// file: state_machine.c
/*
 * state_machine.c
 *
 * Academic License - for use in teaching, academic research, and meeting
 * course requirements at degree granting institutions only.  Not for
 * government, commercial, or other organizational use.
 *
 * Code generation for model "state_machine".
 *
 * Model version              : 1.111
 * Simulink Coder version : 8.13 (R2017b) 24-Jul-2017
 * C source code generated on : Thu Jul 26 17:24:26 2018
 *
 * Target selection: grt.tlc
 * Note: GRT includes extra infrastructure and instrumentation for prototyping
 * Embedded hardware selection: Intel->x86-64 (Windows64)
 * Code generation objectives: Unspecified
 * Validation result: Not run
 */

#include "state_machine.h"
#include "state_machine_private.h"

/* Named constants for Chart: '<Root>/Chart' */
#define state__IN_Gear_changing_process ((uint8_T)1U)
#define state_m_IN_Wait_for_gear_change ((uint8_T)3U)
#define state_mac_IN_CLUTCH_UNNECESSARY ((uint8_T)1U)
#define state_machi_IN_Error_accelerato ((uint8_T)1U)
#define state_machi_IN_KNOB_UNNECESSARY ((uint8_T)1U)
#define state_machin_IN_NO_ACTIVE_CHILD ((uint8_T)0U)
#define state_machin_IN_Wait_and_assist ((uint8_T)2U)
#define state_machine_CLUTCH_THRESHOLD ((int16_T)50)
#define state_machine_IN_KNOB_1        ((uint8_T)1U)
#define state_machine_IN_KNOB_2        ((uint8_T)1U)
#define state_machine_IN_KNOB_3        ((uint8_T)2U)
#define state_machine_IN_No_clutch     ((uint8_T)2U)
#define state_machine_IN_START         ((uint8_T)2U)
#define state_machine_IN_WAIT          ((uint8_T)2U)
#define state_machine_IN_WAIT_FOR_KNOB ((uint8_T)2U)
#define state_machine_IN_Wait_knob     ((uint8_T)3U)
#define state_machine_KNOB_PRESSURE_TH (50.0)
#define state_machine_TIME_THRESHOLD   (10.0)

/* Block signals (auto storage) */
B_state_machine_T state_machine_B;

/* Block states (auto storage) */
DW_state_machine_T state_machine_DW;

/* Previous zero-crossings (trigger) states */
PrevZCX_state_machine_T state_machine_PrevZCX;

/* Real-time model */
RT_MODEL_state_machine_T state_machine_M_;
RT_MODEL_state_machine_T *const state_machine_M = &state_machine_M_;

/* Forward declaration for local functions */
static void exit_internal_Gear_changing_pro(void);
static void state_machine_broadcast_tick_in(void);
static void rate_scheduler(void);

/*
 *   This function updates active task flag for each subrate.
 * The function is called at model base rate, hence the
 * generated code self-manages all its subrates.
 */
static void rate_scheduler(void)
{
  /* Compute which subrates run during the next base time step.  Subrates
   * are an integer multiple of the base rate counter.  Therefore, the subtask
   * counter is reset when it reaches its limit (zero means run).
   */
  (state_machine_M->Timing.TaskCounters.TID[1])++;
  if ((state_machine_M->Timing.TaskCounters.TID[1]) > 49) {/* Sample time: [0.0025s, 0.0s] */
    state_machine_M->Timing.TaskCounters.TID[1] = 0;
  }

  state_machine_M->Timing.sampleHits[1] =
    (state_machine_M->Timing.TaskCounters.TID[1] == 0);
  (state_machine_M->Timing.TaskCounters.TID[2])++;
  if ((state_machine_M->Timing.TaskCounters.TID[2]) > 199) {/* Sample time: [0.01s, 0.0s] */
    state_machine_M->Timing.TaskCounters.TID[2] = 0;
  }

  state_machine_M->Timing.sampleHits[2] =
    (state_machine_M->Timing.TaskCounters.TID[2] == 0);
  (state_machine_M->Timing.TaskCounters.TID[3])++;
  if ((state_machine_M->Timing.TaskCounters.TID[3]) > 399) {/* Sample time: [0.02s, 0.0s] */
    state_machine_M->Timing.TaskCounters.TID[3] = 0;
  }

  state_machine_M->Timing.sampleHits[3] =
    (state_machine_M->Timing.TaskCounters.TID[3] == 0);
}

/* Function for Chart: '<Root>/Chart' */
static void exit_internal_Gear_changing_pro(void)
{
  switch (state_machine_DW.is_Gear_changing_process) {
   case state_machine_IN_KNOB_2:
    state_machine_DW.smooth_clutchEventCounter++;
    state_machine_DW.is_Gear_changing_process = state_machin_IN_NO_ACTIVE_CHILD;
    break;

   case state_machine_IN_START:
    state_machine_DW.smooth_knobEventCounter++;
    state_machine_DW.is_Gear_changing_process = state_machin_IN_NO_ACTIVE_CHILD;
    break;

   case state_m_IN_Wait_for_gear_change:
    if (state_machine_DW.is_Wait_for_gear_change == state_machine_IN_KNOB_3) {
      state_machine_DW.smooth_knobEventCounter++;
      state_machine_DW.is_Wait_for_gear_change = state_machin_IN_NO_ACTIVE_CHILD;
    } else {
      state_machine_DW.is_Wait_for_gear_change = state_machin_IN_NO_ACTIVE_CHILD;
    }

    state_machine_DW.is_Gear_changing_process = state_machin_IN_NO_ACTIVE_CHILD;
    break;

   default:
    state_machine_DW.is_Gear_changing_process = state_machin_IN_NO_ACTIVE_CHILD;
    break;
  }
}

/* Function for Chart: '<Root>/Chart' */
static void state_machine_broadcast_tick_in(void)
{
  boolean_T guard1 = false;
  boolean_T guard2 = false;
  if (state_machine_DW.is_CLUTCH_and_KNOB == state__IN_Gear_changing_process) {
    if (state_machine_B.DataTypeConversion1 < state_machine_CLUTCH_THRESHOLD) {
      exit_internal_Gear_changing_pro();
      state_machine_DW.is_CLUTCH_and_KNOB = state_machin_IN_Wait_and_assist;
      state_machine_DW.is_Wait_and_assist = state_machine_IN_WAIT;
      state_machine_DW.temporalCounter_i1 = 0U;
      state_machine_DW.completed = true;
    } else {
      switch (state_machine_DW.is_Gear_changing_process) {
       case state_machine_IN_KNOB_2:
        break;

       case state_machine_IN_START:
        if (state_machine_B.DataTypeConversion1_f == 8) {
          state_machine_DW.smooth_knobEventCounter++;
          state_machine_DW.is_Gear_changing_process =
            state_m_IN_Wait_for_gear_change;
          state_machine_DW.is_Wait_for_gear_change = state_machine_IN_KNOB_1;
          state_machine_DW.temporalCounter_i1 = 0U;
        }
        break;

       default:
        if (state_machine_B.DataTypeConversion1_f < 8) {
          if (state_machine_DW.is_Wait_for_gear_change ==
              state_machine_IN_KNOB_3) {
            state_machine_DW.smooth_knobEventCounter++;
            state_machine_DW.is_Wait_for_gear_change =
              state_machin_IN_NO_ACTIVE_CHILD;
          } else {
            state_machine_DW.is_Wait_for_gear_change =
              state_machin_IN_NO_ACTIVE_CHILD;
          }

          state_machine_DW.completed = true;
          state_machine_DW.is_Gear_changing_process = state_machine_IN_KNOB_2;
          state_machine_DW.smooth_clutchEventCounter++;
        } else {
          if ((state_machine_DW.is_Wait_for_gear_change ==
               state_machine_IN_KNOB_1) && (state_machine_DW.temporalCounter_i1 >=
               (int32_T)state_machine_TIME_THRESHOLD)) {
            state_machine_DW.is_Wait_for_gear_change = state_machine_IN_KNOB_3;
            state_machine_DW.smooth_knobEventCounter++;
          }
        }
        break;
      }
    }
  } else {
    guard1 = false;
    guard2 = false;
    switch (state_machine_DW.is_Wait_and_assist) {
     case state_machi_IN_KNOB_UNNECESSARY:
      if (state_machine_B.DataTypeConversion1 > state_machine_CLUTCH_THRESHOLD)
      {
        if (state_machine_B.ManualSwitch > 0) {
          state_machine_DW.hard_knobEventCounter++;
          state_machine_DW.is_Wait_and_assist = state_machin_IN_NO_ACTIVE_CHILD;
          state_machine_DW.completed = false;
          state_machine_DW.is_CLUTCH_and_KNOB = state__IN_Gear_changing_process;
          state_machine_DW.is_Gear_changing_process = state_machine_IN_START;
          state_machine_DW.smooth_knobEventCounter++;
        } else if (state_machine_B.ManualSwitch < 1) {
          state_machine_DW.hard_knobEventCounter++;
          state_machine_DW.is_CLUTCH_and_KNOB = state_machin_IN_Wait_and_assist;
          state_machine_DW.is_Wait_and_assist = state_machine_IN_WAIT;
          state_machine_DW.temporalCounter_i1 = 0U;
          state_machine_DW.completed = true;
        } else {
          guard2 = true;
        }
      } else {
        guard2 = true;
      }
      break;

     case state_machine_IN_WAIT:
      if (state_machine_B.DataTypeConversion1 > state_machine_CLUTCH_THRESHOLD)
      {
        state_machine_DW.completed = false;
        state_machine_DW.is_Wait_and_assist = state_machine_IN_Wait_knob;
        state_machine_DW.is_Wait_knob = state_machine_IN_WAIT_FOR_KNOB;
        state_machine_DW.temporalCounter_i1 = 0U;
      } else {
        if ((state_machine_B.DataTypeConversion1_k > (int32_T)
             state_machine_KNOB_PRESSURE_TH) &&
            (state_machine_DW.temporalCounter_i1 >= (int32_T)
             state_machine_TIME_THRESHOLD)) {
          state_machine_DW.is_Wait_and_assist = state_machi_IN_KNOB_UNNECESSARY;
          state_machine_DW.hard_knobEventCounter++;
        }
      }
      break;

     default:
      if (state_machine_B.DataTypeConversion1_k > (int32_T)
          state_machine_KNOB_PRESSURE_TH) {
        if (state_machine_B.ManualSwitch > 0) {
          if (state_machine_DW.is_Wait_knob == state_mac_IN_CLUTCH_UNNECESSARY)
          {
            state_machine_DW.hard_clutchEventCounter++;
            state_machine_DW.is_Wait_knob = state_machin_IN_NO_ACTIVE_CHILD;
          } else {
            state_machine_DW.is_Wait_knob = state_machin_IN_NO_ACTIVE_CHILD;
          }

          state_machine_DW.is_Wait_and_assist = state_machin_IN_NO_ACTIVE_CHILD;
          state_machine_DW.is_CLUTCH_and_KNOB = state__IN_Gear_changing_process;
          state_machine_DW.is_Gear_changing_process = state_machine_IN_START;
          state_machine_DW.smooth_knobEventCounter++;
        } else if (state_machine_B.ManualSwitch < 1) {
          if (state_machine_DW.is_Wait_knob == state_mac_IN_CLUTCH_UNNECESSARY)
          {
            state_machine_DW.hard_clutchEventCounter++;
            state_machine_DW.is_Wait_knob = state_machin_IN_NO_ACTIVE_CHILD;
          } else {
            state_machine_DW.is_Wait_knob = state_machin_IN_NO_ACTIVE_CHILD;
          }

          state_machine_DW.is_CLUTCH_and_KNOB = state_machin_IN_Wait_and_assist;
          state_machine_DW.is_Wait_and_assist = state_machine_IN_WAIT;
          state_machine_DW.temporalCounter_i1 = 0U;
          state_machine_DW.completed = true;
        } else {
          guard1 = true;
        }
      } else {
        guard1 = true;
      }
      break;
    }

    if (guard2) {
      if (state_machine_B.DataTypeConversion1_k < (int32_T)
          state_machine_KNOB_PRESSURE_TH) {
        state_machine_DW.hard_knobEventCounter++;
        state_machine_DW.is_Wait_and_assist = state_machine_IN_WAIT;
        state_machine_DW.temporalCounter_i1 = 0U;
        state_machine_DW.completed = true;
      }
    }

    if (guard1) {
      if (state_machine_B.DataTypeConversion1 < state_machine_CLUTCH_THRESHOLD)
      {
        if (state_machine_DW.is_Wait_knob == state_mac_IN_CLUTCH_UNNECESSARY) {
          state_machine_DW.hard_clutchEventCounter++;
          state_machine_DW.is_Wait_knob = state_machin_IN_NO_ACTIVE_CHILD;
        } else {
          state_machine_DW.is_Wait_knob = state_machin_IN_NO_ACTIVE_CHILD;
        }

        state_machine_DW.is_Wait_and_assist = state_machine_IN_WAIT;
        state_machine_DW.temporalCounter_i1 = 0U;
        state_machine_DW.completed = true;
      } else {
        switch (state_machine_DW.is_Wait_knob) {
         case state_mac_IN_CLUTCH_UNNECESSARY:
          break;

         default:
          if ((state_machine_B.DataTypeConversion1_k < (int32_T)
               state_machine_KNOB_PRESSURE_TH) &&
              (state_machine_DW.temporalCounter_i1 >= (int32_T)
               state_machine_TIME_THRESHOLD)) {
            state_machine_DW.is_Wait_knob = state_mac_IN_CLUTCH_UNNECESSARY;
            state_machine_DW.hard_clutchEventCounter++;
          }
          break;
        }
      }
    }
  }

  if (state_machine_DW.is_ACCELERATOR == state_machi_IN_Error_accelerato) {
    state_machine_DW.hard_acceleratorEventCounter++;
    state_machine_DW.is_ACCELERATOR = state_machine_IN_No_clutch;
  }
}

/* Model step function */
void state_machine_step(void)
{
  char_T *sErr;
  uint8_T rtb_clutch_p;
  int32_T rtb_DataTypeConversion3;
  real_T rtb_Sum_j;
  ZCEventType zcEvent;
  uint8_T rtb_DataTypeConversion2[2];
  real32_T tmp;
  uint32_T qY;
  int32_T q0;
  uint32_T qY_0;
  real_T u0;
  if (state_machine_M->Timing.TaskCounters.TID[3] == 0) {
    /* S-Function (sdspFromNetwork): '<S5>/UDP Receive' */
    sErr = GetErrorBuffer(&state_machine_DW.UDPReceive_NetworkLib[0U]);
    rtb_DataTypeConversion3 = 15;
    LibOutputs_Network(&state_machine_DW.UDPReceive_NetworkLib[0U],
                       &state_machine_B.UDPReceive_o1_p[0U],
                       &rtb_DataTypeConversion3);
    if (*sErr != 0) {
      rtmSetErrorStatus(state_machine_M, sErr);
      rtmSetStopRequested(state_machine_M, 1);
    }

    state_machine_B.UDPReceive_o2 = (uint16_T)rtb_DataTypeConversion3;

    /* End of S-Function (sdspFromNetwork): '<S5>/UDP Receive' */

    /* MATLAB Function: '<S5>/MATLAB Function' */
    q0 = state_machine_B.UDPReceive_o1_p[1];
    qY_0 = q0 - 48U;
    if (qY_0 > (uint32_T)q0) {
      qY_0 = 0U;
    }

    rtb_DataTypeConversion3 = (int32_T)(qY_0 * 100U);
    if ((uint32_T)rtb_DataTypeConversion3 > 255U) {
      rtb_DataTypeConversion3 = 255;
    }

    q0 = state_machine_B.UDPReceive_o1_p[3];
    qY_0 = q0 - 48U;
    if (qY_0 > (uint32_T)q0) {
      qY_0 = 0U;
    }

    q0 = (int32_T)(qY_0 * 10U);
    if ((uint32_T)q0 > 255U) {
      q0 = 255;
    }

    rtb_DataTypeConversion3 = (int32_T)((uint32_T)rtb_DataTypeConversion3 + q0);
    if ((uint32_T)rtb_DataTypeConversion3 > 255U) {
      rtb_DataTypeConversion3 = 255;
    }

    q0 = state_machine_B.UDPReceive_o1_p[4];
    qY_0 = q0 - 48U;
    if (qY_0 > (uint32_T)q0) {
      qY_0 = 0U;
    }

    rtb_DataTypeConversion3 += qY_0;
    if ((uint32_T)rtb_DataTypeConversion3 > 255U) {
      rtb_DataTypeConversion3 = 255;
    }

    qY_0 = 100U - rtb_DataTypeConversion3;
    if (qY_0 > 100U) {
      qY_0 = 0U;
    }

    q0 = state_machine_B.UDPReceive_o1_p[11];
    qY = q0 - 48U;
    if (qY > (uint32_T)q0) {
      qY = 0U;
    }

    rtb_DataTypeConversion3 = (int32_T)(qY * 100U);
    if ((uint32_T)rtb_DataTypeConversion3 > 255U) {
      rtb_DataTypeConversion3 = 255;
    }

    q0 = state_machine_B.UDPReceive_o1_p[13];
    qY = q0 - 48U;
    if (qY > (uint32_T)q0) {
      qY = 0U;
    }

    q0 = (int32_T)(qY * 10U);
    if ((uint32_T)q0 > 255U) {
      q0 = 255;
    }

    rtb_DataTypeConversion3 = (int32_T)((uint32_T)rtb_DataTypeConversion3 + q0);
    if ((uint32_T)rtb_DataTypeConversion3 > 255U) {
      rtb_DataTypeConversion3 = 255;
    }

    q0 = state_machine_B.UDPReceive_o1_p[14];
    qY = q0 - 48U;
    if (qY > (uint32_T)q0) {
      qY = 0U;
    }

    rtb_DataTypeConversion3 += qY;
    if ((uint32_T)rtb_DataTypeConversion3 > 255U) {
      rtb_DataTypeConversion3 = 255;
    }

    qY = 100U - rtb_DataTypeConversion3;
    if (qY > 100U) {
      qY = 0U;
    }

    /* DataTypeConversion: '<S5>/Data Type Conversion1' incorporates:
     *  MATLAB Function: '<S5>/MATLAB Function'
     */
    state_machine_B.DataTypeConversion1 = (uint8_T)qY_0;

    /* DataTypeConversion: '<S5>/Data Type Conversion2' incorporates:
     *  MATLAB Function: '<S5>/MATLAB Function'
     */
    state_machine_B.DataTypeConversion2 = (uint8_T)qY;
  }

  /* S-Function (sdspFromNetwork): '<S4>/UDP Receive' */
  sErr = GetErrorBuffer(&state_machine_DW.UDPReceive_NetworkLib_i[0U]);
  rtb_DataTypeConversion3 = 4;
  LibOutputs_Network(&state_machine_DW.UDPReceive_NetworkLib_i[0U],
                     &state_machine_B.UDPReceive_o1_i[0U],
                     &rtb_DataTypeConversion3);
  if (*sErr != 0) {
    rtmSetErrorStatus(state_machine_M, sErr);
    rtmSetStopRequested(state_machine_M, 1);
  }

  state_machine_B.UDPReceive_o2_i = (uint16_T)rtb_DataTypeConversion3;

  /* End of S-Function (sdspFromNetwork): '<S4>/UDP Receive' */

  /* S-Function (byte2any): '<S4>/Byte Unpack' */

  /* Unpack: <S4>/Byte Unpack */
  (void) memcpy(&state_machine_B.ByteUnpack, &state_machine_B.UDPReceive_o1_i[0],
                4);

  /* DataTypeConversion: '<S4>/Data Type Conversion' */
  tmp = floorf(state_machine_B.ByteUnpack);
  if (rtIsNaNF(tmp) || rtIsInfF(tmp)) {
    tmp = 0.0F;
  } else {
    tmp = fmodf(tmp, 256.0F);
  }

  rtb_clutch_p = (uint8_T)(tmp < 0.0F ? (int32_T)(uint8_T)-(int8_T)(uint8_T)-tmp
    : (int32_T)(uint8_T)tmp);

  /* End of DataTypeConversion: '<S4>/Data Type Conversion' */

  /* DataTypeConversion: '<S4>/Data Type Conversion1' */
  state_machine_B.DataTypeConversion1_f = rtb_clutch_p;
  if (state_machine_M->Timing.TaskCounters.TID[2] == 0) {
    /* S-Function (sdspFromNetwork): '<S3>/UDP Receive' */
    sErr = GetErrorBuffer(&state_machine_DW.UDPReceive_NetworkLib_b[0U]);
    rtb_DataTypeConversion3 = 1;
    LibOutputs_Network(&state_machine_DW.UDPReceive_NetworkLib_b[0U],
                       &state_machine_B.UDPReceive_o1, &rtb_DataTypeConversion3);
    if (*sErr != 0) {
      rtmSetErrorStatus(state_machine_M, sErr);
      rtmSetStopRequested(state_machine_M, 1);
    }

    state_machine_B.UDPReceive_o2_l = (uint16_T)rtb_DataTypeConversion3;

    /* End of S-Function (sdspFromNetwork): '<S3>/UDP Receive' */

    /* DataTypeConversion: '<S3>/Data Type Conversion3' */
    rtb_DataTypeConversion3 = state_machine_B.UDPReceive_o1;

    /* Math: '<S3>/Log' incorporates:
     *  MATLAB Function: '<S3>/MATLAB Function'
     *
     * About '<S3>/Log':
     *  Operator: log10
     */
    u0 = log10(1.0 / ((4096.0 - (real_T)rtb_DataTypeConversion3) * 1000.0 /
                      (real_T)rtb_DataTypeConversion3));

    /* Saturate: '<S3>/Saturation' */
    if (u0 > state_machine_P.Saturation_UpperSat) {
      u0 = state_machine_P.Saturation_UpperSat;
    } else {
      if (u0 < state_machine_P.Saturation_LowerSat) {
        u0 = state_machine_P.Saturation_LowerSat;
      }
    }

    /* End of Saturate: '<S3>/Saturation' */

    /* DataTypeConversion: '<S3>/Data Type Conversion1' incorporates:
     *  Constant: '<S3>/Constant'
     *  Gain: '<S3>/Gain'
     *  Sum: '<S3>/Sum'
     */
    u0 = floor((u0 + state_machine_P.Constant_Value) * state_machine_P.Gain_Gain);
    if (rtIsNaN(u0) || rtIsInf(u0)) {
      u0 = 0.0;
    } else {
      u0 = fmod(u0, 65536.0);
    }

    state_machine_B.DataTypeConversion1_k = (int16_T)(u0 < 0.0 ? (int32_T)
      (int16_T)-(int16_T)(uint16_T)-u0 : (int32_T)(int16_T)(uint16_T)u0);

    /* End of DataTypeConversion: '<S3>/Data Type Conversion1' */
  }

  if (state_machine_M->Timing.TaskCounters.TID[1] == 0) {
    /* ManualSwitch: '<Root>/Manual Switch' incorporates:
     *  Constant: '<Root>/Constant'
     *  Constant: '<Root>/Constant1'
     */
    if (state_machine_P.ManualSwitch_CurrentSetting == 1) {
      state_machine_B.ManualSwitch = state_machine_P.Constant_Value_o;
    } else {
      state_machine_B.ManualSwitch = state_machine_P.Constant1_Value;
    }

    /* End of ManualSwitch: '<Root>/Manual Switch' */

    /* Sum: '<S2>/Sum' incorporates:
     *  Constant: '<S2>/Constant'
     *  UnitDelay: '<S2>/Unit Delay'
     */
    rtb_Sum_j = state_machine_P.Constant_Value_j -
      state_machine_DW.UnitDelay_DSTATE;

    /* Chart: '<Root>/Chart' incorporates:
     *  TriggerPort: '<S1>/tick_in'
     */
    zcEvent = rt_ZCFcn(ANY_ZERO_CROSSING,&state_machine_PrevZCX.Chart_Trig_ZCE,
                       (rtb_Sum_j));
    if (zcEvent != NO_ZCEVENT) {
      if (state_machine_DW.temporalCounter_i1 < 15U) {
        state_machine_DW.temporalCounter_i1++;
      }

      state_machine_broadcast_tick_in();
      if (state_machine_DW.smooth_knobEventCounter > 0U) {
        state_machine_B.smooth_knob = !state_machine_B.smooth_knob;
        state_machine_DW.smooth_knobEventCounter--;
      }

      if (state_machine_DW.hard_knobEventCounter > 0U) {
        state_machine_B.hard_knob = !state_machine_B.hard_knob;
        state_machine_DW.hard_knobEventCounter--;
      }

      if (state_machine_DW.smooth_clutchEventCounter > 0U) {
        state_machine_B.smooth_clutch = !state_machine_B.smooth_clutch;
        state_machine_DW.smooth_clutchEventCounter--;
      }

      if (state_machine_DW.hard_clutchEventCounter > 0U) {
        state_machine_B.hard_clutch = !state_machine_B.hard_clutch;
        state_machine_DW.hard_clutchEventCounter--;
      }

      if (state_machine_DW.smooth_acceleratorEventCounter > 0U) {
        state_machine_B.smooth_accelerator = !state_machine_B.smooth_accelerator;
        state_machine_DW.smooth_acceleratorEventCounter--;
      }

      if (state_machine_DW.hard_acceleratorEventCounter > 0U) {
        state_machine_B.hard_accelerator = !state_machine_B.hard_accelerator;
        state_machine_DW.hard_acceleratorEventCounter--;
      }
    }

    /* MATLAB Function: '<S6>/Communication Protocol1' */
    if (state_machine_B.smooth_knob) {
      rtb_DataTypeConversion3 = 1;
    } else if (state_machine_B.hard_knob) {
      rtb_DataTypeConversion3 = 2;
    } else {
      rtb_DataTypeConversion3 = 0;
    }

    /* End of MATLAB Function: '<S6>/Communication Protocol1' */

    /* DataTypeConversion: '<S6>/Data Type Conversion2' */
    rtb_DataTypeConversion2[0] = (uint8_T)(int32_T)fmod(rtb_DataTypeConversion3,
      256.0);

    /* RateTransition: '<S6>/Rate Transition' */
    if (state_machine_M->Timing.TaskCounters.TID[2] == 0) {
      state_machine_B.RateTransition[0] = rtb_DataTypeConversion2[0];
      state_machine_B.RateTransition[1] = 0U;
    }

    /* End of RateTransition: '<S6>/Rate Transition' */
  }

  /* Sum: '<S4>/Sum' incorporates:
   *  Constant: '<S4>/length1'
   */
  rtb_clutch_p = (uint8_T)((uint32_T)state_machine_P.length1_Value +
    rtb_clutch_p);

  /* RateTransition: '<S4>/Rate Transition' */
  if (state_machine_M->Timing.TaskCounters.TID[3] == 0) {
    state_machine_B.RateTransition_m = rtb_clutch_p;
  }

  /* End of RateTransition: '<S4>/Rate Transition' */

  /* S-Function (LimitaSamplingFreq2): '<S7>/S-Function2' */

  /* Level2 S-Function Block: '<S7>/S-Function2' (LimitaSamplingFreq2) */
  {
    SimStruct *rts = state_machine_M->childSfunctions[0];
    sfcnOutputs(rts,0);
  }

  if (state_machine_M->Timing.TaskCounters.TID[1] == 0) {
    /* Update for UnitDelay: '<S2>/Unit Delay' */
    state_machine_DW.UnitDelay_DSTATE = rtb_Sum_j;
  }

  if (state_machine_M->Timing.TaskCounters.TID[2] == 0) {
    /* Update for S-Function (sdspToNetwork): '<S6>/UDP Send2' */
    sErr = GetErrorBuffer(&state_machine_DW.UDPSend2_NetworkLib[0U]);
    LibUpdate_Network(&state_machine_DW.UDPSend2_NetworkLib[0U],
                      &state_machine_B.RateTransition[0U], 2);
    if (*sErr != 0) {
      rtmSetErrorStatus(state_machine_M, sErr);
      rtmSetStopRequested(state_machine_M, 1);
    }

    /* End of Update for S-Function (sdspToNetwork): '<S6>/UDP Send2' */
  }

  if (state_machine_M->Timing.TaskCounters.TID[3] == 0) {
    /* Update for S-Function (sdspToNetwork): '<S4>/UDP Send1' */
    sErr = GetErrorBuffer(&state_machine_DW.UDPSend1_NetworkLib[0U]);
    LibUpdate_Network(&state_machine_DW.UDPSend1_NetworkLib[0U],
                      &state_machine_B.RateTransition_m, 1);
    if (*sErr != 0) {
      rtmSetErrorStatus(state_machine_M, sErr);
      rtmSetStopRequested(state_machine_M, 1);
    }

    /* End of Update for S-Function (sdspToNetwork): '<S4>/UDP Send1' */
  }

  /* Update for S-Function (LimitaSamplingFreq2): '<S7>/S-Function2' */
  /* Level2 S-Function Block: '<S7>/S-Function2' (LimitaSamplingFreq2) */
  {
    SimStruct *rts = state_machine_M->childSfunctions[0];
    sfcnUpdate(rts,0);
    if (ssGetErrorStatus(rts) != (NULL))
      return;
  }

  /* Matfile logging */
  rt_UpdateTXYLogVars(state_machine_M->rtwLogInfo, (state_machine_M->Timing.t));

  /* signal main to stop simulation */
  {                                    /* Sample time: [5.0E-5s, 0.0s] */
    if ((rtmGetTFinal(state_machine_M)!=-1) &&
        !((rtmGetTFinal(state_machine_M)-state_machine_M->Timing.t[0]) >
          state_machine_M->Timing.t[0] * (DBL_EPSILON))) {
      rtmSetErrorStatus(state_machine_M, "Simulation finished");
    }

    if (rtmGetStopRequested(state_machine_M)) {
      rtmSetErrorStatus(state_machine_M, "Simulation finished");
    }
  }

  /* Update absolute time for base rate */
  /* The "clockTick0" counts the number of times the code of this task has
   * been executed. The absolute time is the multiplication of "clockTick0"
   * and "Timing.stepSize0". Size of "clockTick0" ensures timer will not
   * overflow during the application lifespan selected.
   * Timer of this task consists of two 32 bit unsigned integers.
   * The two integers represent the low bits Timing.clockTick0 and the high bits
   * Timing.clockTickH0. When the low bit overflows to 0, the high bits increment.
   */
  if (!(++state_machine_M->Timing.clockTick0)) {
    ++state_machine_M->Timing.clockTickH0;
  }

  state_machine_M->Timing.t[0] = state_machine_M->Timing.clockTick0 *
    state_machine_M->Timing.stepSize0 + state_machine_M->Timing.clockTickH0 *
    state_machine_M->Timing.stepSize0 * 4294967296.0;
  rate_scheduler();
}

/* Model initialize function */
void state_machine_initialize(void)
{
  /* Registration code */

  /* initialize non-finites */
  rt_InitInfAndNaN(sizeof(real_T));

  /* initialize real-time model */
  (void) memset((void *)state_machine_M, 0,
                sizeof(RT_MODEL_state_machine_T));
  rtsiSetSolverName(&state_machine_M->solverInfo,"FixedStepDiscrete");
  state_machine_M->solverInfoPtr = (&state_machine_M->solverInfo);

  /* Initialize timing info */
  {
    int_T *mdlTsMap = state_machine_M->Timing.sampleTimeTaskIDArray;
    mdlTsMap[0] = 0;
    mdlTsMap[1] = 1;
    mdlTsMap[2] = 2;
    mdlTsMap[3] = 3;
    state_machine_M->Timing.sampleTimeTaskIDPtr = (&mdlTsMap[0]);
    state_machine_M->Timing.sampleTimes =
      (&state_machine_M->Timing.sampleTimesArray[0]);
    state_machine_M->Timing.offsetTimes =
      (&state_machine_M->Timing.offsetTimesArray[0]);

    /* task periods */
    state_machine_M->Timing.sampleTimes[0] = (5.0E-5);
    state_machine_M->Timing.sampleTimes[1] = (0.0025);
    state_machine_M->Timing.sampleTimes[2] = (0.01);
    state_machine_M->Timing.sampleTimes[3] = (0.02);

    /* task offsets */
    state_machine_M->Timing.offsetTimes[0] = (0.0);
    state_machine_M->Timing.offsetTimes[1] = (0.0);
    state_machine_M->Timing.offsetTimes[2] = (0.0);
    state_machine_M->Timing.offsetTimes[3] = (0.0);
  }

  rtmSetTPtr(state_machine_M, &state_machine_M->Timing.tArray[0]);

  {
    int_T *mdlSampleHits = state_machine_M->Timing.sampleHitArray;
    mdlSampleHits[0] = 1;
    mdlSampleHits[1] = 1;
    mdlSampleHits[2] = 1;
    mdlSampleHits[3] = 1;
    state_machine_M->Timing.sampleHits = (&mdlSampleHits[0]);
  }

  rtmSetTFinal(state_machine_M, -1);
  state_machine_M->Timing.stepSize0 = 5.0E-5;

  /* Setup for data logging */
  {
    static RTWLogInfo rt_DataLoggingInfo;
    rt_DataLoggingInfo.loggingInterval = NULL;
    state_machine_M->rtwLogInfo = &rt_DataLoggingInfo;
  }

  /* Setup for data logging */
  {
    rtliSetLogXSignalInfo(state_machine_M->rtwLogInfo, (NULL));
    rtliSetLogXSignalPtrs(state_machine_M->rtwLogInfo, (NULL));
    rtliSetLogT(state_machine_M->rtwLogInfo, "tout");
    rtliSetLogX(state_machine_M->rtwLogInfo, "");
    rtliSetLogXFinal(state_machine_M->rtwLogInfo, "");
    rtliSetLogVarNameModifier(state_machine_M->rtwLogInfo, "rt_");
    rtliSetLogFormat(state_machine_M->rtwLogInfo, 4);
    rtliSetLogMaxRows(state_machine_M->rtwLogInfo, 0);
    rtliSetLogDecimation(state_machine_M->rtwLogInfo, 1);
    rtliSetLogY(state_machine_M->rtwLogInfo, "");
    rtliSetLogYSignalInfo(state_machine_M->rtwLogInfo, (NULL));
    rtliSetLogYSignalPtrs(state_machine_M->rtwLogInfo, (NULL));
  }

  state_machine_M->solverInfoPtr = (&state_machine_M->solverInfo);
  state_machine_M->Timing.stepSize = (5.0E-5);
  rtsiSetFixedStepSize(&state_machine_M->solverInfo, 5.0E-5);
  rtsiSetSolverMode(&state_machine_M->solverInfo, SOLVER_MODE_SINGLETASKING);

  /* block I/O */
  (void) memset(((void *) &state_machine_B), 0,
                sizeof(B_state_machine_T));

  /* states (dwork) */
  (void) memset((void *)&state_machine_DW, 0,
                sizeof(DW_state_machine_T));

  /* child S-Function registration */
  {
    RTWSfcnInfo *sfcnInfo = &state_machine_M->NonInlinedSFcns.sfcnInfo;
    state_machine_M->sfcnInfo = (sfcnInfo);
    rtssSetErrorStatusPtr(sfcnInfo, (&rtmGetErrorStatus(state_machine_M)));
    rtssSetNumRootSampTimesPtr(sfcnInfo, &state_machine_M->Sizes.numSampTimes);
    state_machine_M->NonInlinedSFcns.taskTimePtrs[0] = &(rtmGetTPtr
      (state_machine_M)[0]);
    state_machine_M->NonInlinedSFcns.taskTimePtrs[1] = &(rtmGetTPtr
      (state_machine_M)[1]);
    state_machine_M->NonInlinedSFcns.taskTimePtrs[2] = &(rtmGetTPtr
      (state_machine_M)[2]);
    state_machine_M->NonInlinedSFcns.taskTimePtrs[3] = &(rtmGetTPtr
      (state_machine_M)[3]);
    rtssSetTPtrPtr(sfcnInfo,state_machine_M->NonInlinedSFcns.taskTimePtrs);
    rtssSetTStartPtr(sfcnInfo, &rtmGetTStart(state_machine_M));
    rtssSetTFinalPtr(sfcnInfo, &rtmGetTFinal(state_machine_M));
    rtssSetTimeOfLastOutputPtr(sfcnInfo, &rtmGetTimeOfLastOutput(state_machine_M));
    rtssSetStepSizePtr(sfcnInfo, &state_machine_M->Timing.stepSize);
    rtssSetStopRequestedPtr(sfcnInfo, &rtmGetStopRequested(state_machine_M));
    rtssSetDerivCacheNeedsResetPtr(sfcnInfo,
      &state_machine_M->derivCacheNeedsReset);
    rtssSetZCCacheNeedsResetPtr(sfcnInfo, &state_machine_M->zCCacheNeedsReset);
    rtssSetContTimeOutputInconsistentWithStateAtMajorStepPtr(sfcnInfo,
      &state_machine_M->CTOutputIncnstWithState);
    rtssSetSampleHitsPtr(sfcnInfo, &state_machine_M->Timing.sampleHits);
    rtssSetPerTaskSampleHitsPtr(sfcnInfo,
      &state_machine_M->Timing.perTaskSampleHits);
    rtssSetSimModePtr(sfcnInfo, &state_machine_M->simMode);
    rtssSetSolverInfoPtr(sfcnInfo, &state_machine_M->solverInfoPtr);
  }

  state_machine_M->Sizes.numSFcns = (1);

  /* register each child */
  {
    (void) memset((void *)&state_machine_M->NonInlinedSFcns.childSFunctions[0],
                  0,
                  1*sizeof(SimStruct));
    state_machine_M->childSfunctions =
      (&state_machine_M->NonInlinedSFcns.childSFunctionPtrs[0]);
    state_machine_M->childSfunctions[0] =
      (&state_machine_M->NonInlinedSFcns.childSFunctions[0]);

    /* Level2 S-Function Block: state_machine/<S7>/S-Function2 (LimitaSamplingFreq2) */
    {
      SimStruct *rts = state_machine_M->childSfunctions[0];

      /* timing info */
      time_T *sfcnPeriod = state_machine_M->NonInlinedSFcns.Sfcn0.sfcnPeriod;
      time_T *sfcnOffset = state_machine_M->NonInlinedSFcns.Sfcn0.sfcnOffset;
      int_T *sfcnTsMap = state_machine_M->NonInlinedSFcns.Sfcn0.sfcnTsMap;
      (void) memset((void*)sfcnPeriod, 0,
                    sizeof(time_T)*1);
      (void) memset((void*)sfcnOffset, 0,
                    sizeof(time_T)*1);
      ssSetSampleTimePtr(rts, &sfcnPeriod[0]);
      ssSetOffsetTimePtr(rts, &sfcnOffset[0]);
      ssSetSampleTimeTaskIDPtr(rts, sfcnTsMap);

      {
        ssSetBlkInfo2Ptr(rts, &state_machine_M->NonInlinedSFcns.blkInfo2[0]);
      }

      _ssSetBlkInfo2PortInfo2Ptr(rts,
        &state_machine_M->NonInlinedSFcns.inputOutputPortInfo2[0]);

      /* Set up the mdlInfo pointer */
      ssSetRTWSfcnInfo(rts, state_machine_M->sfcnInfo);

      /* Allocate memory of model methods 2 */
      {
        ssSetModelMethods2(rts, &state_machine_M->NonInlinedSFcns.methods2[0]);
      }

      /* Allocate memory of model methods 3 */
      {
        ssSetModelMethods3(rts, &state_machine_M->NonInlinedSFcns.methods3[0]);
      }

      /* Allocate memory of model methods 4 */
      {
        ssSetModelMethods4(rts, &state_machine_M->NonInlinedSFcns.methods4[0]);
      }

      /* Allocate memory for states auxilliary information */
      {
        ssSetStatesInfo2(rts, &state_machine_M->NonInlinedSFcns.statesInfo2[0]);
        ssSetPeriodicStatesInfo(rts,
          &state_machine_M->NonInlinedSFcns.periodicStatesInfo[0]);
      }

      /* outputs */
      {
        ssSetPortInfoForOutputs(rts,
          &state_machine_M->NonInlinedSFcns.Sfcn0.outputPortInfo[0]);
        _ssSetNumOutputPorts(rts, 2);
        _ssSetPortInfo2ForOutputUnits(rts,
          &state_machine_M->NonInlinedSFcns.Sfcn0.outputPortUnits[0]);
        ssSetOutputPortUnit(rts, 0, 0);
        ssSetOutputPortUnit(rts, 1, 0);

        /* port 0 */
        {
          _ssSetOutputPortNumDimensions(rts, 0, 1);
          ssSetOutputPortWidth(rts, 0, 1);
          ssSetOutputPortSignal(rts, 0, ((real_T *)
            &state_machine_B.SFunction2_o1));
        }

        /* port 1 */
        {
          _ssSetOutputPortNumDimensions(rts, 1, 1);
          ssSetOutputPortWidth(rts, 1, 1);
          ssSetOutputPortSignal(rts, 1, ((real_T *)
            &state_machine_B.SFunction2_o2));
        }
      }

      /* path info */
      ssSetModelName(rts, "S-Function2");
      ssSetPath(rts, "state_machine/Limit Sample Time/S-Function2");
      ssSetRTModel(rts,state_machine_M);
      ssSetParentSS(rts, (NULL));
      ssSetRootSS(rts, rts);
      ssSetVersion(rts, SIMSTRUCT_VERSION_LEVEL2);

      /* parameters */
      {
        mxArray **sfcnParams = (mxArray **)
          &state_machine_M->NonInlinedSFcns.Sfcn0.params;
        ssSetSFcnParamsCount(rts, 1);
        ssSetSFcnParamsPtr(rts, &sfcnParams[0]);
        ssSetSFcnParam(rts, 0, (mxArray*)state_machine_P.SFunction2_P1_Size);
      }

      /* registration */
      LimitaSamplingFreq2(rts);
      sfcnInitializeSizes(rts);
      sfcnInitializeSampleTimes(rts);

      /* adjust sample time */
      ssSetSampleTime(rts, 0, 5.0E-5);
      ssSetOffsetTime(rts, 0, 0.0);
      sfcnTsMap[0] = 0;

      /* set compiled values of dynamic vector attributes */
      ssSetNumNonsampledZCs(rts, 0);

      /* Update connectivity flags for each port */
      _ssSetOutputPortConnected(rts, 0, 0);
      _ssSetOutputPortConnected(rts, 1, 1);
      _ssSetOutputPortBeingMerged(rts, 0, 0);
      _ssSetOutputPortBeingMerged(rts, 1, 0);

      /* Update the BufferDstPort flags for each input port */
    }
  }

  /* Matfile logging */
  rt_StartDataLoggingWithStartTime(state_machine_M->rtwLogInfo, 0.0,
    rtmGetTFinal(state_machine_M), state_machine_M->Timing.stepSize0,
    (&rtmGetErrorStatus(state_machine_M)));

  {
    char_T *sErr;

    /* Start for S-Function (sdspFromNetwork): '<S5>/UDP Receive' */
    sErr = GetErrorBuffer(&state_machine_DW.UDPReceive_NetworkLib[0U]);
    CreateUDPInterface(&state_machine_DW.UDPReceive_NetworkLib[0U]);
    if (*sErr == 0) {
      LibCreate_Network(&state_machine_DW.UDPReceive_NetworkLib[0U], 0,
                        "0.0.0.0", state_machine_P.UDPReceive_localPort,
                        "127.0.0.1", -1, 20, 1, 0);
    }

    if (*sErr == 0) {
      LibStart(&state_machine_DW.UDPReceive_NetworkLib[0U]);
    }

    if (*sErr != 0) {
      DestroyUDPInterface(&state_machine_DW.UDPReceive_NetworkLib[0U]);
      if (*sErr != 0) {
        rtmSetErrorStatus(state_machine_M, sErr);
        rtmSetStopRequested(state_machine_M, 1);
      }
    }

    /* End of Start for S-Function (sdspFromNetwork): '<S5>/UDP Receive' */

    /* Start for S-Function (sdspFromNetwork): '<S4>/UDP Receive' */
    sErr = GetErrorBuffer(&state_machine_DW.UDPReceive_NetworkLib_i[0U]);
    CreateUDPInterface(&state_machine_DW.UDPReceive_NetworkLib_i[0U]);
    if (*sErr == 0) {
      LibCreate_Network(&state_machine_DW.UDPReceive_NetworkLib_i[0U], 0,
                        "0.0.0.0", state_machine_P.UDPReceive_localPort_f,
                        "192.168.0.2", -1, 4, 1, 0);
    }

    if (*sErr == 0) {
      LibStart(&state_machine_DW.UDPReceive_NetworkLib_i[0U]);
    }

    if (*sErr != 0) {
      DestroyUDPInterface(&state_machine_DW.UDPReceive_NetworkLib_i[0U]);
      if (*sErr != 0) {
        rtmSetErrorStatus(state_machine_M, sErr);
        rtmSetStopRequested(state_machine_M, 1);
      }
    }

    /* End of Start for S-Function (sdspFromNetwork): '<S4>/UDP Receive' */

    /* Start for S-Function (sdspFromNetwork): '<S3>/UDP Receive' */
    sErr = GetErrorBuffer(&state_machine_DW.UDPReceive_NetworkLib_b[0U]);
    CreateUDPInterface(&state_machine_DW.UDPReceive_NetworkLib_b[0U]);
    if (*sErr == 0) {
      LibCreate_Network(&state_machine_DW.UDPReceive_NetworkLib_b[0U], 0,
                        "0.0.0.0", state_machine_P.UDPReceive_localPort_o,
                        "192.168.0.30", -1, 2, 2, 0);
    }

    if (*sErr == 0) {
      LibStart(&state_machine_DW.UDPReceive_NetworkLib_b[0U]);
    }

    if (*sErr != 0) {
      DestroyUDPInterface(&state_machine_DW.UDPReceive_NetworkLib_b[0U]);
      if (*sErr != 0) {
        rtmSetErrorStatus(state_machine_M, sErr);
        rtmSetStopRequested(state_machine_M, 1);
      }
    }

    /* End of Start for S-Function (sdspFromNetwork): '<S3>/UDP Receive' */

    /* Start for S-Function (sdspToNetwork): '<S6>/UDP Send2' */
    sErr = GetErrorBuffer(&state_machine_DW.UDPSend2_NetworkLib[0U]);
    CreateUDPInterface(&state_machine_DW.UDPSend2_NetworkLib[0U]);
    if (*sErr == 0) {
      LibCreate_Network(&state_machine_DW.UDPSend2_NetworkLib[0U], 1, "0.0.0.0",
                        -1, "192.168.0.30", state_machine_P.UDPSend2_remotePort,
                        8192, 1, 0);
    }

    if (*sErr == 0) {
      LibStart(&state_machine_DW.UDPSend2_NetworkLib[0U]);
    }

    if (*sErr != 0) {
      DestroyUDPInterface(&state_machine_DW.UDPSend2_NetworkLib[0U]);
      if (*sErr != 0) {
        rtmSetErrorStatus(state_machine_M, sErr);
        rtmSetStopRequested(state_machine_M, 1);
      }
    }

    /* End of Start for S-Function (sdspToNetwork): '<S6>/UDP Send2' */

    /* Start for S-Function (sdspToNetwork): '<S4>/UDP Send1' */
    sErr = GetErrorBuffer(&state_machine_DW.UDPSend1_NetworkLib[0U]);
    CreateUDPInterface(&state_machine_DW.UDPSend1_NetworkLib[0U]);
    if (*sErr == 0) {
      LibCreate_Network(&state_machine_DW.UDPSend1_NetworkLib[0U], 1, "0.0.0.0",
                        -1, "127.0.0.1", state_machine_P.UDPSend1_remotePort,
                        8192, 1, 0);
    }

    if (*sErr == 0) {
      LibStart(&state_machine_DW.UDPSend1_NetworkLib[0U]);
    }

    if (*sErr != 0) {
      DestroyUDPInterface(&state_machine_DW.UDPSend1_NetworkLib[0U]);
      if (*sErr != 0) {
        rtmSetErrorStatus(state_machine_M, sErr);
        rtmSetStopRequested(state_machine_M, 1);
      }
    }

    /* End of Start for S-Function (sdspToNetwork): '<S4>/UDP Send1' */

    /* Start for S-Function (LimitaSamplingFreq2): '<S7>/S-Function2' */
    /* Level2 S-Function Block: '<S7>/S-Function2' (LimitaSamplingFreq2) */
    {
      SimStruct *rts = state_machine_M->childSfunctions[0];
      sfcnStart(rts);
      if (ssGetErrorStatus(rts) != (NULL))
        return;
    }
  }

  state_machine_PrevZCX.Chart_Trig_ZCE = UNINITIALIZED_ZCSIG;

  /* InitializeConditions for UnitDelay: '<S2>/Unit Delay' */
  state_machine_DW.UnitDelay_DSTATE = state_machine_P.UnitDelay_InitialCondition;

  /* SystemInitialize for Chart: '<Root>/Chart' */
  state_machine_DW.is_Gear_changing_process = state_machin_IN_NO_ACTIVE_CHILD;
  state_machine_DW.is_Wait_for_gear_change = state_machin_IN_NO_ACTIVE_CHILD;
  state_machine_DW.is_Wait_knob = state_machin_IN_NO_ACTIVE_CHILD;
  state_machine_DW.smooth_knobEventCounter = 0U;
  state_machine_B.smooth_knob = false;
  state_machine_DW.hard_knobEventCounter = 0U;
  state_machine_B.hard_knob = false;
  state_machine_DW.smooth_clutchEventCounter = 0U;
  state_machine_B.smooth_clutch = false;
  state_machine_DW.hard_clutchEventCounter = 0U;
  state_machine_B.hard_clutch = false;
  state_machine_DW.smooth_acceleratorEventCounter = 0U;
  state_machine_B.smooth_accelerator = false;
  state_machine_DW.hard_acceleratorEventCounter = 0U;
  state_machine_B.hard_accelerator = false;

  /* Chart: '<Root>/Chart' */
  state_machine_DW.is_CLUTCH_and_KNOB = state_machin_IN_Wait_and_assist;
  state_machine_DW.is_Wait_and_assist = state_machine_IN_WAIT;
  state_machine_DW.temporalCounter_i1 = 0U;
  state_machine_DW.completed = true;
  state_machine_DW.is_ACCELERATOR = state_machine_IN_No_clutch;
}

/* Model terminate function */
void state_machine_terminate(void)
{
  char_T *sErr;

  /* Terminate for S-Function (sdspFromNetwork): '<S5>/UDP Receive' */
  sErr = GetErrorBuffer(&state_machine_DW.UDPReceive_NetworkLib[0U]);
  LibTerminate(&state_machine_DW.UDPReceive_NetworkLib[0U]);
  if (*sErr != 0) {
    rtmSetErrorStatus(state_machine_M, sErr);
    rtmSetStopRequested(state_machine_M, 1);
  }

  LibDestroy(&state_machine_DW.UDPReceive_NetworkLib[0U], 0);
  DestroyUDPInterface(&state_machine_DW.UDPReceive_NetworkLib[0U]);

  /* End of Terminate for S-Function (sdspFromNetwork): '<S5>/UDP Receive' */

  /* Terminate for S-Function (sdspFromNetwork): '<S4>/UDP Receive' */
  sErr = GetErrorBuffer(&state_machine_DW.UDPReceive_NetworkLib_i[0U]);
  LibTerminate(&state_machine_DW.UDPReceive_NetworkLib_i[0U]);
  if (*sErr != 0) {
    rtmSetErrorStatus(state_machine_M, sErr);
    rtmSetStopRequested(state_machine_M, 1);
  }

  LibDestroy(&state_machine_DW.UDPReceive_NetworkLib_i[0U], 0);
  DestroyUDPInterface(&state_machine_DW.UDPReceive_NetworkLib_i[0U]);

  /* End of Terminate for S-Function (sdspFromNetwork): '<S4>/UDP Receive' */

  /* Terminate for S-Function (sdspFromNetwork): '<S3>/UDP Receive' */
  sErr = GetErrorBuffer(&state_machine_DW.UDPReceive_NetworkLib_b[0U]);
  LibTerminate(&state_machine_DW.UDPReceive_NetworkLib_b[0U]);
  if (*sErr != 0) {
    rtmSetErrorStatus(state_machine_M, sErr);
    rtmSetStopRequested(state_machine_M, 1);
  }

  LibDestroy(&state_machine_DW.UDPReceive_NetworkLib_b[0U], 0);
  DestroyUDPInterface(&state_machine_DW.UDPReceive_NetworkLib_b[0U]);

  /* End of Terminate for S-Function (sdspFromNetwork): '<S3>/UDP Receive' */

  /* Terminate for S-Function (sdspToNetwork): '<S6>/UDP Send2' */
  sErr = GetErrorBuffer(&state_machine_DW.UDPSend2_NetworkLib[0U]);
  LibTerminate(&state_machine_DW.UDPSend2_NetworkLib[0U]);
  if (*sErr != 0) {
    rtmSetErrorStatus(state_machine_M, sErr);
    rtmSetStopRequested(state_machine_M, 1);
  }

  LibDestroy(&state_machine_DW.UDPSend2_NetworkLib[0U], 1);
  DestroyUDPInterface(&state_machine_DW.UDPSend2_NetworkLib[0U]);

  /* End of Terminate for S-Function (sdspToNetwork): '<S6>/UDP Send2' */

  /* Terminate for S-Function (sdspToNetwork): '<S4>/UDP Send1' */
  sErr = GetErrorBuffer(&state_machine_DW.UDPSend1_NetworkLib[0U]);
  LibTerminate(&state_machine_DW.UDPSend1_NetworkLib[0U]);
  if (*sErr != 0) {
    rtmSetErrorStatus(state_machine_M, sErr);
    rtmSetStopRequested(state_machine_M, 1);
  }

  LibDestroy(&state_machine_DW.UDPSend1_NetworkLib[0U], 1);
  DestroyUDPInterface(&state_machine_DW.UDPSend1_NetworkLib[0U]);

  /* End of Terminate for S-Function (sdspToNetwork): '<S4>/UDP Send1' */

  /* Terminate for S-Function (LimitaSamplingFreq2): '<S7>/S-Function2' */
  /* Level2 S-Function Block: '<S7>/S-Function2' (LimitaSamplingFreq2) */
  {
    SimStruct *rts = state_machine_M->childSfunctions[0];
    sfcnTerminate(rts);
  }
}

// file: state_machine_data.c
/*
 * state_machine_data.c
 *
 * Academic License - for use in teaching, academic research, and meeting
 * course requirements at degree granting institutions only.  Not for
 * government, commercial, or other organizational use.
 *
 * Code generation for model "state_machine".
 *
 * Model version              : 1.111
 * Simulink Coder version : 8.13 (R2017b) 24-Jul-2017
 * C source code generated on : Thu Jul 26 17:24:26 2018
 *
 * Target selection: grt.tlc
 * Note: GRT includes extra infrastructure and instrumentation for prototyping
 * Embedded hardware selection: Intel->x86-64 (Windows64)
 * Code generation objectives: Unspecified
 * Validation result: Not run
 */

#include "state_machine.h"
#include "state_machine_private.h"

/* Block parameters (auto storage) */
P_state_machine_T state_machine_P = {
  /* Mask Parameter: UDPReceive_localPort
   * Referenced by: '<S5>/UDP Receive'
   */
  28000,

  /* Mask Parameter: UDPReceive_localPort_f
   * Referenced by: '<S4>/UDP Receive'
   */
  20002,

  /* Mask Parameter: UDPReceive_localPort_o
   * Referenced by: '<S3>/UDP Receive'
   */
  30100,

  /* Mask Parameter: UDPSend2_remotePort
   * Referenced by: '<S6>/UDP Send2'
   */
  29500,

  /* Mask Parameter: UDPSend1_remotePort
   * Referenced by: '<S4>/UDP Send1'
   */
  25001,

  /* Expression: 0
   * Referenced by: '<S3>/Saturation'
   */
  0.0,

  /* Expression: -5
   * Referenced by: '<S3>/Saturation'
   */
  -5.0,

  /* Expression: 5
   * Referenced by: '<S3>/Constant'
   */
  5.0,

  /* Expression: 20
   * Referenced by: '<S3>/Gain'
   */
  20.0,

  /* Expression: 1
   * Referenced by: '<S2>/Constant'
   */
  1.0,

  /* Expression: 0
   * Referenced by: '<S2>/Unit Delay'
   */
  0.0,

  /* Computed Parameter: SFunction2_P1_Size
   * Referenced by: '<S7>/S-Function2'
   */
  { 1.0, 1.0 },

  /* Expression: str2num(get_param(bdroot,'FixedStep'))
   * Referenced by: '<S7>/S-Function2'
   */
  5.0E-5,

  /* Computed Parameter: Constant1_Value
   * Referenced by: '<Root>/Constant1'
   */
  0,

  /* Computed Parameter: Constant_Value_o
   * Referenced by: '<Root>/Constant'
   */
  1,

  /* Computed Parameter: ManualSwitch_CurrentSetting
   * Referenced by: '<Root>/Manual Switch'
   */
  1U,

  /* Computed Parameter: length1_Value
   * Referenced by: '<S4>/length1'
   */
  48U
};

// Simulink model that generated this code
simulink model "state_machine"  (R2017b)
settings: Solver=FixedStepDiscrete  StartTime=0.0  StopTime=inf  FixedStep=0.00005  RelTol=1e-3
libraries: dspnetwork x5, simulink_extras x1, etargetslib x1, xpcrtudplib x1

== system state_machine ==
  note: State Machine of the Student Challenge of Asiahaptics 2018
  Chart : Stateflow chart  TreatAsAtomicUnit=on
  Clock1 : simulink_extras/Flip Flops/Clock  period=0.005
  Constant : Constant  OutDataTypeStr=int16
  Constant1 : Constant  Value=0  OutDataTypeStr=int16
  Display{2..5} (4 alike) : Display
  Get Knob Pressure : Subsystem
  Get gear : Subsystem
  Get pedals : Subsystem
  KNOB : Subsystem
  Limit Sample Time : Subsystem
  Manual Switch : ManualSwitch
  Terminator : Terminator
  wires:
  Clock1/1 -> Chart/Trigger
  Chart/3(smooth_clutch) -> Display2/1
  Chart/4(hard_clutch) -> Display3/1
  Chart/5(smooth_accelerator) -> Display4/1
  Chart/6(hard_accelerator) -> Display5/1
  Constant/1 -> Manual Switch/1
  Constant1/1 -> Manual Switch/2
  Manual Switch/1 -> Chart/7(assistive_changing)
  Get pedals/1(clutch) -> Chart/1(clutch_pedal)
  Get pedals/2(accelerator) -> Chart/2(accelerator_pedal)
  Get pedals/3("break ") -> Terminator/1
  Get gear/1(gear) -> Chart/3(gear)
  Chart/1(smooth_knob) -> KNOB/1(smooth)
  Chart/2(hard_knob) -> KNOB/2(hard)
  Get Knob Pressure/1(knob_pressure) -> Chart/6(knob_pressure)

== system state_machine/Get Knob Pressure ==
  Constant : Constant  Value=5
  Data Type Conversion1 : DataTypeConversion  OutDataTypeStr=int16
  Data Type Conversion3 : DataTypeConversion  OutDataTypeStr=double
  Display : Display
  Display1 : Display
  Display2 : Display
  Gain : Gain  Gain=20
  Log : Math  Operator=log10  SaturateOnIntegerOverflow=on
  MATLAB Function : MATLAB Function  TreatAsAtomicUnit=on
  Saturation : Saturate  UpperLimit=0  LowerLimit=-5
  Sum : Sum  Inputs=|++
  Terminator1 : Terminator
  UDP Receive : dspnetwork/UDP Receive  localURL='0.0.0.0'  localPort=30100  remoteURL='192.168.0.30'  remotePort=-1  recvBufferSize=2  dims=1  signalDatatype=int16  isVarSize=off  showBlockingTime=off  blockingTime=0  sampletime=0.01  blockPlatform=[]
  knob_pressure : Outport
  wires:
  UDP Receive/2 -> Terminator1/1
  UDP Receive/1 -> Data Type Conversion3/1, Display/1
  Log/1 -> Saturation/1
  Data Type Conversion1/1 -> knob_pressure/1
  MATLAB Function/2(res_inv) -> Log/1
  Gain/1 -> Display1/1, Data Type Conversion1/1
  MATLAB Function/1(res) -> Display2/1
  Data Type Conversion3/1 -> MATLAB Function/1(udp_msg)
  Saturation/1 -> Sum/1
  Sum/1 -> Gain/1
  Constant/1 -> Sum/2

== system state_machine/Get gear ==
  Byte Unpack : etargetslib/Byte Unpack  dimensions={[1]}  datatypes={'single'}  byteAlign=1
  Data Type Conversion : DataTypeConversion  OutDataTypeStr=uint8
  Data Type Conversion1 : DataTypeConversion  OutDataTypeStr=int16
  Display6 : Display
  Display7 : Display
  Rate Transition : RateTransition  OutPortSampleTime=0.02
  Sum : Sum  Inputs=++|
  Terminator : Terminator
  UDP Receive : dspnetwork/UDP Receive  localURL='0.0.0.0'  localPort=20002  remoteURL='192.168.0.2'  remotePort=-1  recvBufferSize=4  dims=4  signalDatatype=uint8  isVarSize=off  showBlockingTime=off  blockingTime=0  sampletime=0.00005  blockPlatform=[]
  UDP Receive2 : xpcrtudplib/UDP Receive  Commented=on  ipAddressVal=Use host-target connection  localPort=20002  rcvWidth=4  rcvFmAny=off  fmAddress=192.168.0.2  maxUDPQueue=8  sampleTime=0.00005
  UDP Send1 : dspnetwork/UDP Send  remoteURL='127.0.0.1'  remotePort=25001  localURL='0.0.0.0'  localPortSource=Automatically determine  localPort=-1  sampletime=-1  blockPlatform=[]  separateLengthPort=0
  length1 : Constant  Value=48  OutDataTypeStr=uint8
  gear : Outport
  wires:
  UDP Receive/2 -> Terminator/1
  Sum/1 -> Rate Transition/1
  Byte Unpack/1 -> Display6/1, Data Type Conversion/1
  Rate Transition/1 -> UDP Send1/1
  UDP Receive/1 -> Byte Unpack/1
  length1/1 -> Sum/1
  Data Type Conversion/1 -> Data Type Conversion1/1, Sum/2, Display7/1
  Data Type Conversion1/1 -> gear/1

== system state_machine/Get pedals ==
  Data Type Conversion1 : DataTypeConversion  OutDataTypeStr=int16
  Data Type Conversion2 : DataTypeConversion  OutDataTypeStr=int16
  Display6 : Display
  Display7 : Display
  Display8 : Display
  MATLAB Function : MATLAB Function  TreatAsAtomicUnit=on
  Terminator : Terminator
  UDP Receive : dspnetwork/UDP Receive  localURL='0.0.0.0'  localPort=28000  remoteURL='127.0.0.1'  remotePort=-1  recvBufferSize=20  dims=15  signalDatatype=uint8  isVarSize=off  showBlockingTime=off  blockingTime=0  sampletime=0.02  blockPlatform=[]
  clutch : Outport
  accelerator : Outport  Port=2
  "break " : Outport  Port=3
  wires:
  Data Type Conversion1/1 -> clutch/1
  MATLAB Function/1(clutch_p) -> Data Type Conversion1/1, Display6/1
  MATLAB Function/2(break_p) -> "break "/1, Display7/1
  UDP Receive/1 -> MATLAB Function/1(udp_msg)
  MATLAB Function/3(acc_p) -> Data Type Conversion2/1, Display8/1
  UDP Receive/2 -> Terminator/1
  Data Type Conversion2/1 -> accelerator/1

== system state_machine/KNOB ==
  smooth : Inport
  hard : Inport  Port=2
  Communication Protocol1 : MATLAB Function  TreatAsAtomicUnit=on
  Data Type Conversion2 : DataTypeConversion  OutDataTypeStr=uint8
  Rate Transition : RateTransition  OutPortSampleTime=0.01
  UDP Send2 : dspnetwork/UDP Send  remoteURL='192.168.0.30'  remotePort=29500  localURL='0.0.0.0'  localPortSource=Automatically determine  localPort=-1  sampletime=-1  blockPlatform=[]  separateLengthPort=0
  wires:
  Communication Protocol1/1(msg_out) -> Data Type Conversion2/1
  Rate Transition/1 -> UDP Send2/1
  Data Type Conversion2/1 -> Rate Transition/1
  smooth/1 -> Communication Protocol1/1(smooth)
  hard/1 -> Communication Protocol1/2(hard)

== system state_machine/Limit Sample Time ==
  note: Host PC Time
  Display6 : Display
  S-Function2 : S-Function  FunctionName=LimitaSamplingFreq2  Parameters=str2num(get_param(bdroot,'FixedStep'))  SFunctionDeploymentMode=off  EnableBusSupport=off
  Terminator3 : Terminator
  tag scope: hostPcTime=global
  wires:
  S-Function2/1 -> Terminator3/1
  S-Function2/2 -> [hostPcTime], Display6/1

== matlab function state_machine/Get Knob Pressure/MATLAB Function ==
function [res,res_inv]  = get_FSR_resistance(udp_msg)
%% The function returns the value of the FSR resistance
% starting from the ADC value (the signal passes through a voltage divider
r_in = 1000, % Ohm
V_in = 4096; % ADC ticks
V_out = udp_msg; % ADC ticks

res = r_in * (V_in - V_out) / V_out;
res_inv = 1/res;
end

== matlab function state_machine/Get pedals/MATLAB Function ==
function [clutch_p, break_p, acc_p] = get_pedals(udp_msg)
%% The function provides the values of pression of the pedals
%  as an integer number between 0 and 100 (0 released, 100 completely
%  pressed)

clutch_p = 100 - (get_number(udp_msg(2))*100 + get_number(udp_msg(4))*10 + get_number(udp_msg(5)));
break_p = 100 - (get_number(udp_msg(7))*100 + get_number(udp_msg(9))*10 + get_number(udp_msg(10)));
acc_p = 100 - (get_number(udp_msg(12))*100 + get_number(udp_msg(14))*10 + get_number(udp_msg(15)));

end

function [number] = get_number(char)
    number = char - 48;
end

== stateflow chart state_machine/Chart ==
  settings: executeAtInitialization=1
  state CLUTCH_and_KNOB [parallel]
    settings: executionOrder=1
    state Gear_changing_process
      % This Part is assistive driving and can be deactivated if necessary
      state START
        % The system waits for the knob_action
        entry:smooth_knob
        exit:smooth_knob
      state Wait_for_gear_change
        state KNOB_1
          % The action of change starts
          % Neutral Gear
        state KNOB_3
          % The driver waits a lot to change
          entry:smooth_knob
          exit:smooth_knob
        KNOB_1 -> KNOB_3 : after(TIME_THRESHOLD,tick_in)
      state KNOB_2
        % The driver changes the gear
        entry:smooth_clutch
        exit:smooth_clutch
      (default) -> START
      START -> KNOB_1 : [gear==8]
      Wait_for_gear_change -> KNOB_2 : [gear<8]/{completed=true}
    state Wait_and_assist
      state WAIT
        entry: completed=true
      state Wait_knob
        state WAIT_FOR_KNOB
          % The driver should hold
          % the knob
        state CLUTCH_UNNECESSARY
          entry:hard_clutch
          exit:hard_clutch
        (default) -> WAIT_FOR_KNOB
        WAIT_FOR_KNOB -> CLUTCH_UNNECESSARY : [knob_pressure < KNOB_PRESSURE_TH & after(TIME_THRESHOLD,tick_in)]
      state KNOB_UNNECESSARY
        entry: hard_knob
        exit: hard_knob
      (default) -> WAIT
      WAIT -> Wait_knob [order 1] : [clutch_pedal > CLUTCH_THRESHOLD]/{completed=false}
      KNOB_UNNECESSARY -> WAIT [order 2] : [knob_pressure < KNOB_PRESSURE_TH]
      WAIT -> KNOB_UNNECESSARY [order 2] : [knob_pressure > KNOB_PRESSURE_TH & after(TIME_THRESHOLD,tick_in)]
      Wait_knob -> WAIT [order 2] : [clutch_pedal < CLUTCH_THRESHOLD]
    (default) -> Wait_and_assist
    Gear_changing_process -> WAIT : [clutch_pedal < CLUTCH_THRESHOLD]
    Wait_knob -> (junction 83) [order 1] : [knob_pressure > KNOB_PRESSURE_TH]
    (junction 83) -> Gear_changing_process [order 1] : [assistive_changing > 0]
    KNOB_UNNECESSARY -> (junction 83) [order 1] : [clutch_pedal > CLUTCH_THRESHOLD]/{completed=false}
    (junction 83) -> Wait_and_assist [order 2] : [assistive_changing < 1]
  state ACCELERATOR [parallel]
    settings: executionOrder=2
    state No_clutch
    state Error_accelerato
      entry: hard_accelerator
      exit: hard_accelerator
    No_clutch -> Error_accelerato : [completed==false & accelerator_pressure > ACCELERATOR_PRESSURE_TS]
    (default) -> No_clutch
    Error_accelerato -> No_clutch : [completed==true | accelerator_pressure < ACCELERATOR_PRESSURE_TS]
  data: clutch_pedal input int16; accelerator_pedal input int16; gear input int16; clutch_pressure input int16; accelerator_pressure input int16; knob_pressure input int16; CLUTCH_THRESHOLD constant int16 =50; TIME_THRESHOLD constant double =10; KNOB_PRESSURE_TH constant double =50; assistive_changing input int16; completed local boolean =true; ACCELERATOR_PRESSURE_TS constant int16 =10
  events: smooth_knob output EITHER_EDGE_EVENT; hard_knob output EITHER_EDGE_EVENT; smooth_clutch output EITHER_EDGE_EVENT; hard_clutch output EITHER_EDGE_EVENT; smooth_accelerator output EITHER_EDGE_EVENT; hard_accelerator output EITHER_EDGE_EVENT; tick_in input EITHER_EDGE_EVENT

== matlab function state_machine/KNOB/Communication Protocol1 ==
function msg_out  = generate_msg(smooth, hard)
%% The function generate the message depending on the state
msg = zeros(2,1);
if (smooth == 1)
    msg(1) = 1;
    msg(2) = 0;
else if (hard == 1)
        msg(1) = 2;
        msg(2) = 0;
    else
        msg(1) = 0;
        msg(2) = 0;
    end
end

msg_out = msg;
